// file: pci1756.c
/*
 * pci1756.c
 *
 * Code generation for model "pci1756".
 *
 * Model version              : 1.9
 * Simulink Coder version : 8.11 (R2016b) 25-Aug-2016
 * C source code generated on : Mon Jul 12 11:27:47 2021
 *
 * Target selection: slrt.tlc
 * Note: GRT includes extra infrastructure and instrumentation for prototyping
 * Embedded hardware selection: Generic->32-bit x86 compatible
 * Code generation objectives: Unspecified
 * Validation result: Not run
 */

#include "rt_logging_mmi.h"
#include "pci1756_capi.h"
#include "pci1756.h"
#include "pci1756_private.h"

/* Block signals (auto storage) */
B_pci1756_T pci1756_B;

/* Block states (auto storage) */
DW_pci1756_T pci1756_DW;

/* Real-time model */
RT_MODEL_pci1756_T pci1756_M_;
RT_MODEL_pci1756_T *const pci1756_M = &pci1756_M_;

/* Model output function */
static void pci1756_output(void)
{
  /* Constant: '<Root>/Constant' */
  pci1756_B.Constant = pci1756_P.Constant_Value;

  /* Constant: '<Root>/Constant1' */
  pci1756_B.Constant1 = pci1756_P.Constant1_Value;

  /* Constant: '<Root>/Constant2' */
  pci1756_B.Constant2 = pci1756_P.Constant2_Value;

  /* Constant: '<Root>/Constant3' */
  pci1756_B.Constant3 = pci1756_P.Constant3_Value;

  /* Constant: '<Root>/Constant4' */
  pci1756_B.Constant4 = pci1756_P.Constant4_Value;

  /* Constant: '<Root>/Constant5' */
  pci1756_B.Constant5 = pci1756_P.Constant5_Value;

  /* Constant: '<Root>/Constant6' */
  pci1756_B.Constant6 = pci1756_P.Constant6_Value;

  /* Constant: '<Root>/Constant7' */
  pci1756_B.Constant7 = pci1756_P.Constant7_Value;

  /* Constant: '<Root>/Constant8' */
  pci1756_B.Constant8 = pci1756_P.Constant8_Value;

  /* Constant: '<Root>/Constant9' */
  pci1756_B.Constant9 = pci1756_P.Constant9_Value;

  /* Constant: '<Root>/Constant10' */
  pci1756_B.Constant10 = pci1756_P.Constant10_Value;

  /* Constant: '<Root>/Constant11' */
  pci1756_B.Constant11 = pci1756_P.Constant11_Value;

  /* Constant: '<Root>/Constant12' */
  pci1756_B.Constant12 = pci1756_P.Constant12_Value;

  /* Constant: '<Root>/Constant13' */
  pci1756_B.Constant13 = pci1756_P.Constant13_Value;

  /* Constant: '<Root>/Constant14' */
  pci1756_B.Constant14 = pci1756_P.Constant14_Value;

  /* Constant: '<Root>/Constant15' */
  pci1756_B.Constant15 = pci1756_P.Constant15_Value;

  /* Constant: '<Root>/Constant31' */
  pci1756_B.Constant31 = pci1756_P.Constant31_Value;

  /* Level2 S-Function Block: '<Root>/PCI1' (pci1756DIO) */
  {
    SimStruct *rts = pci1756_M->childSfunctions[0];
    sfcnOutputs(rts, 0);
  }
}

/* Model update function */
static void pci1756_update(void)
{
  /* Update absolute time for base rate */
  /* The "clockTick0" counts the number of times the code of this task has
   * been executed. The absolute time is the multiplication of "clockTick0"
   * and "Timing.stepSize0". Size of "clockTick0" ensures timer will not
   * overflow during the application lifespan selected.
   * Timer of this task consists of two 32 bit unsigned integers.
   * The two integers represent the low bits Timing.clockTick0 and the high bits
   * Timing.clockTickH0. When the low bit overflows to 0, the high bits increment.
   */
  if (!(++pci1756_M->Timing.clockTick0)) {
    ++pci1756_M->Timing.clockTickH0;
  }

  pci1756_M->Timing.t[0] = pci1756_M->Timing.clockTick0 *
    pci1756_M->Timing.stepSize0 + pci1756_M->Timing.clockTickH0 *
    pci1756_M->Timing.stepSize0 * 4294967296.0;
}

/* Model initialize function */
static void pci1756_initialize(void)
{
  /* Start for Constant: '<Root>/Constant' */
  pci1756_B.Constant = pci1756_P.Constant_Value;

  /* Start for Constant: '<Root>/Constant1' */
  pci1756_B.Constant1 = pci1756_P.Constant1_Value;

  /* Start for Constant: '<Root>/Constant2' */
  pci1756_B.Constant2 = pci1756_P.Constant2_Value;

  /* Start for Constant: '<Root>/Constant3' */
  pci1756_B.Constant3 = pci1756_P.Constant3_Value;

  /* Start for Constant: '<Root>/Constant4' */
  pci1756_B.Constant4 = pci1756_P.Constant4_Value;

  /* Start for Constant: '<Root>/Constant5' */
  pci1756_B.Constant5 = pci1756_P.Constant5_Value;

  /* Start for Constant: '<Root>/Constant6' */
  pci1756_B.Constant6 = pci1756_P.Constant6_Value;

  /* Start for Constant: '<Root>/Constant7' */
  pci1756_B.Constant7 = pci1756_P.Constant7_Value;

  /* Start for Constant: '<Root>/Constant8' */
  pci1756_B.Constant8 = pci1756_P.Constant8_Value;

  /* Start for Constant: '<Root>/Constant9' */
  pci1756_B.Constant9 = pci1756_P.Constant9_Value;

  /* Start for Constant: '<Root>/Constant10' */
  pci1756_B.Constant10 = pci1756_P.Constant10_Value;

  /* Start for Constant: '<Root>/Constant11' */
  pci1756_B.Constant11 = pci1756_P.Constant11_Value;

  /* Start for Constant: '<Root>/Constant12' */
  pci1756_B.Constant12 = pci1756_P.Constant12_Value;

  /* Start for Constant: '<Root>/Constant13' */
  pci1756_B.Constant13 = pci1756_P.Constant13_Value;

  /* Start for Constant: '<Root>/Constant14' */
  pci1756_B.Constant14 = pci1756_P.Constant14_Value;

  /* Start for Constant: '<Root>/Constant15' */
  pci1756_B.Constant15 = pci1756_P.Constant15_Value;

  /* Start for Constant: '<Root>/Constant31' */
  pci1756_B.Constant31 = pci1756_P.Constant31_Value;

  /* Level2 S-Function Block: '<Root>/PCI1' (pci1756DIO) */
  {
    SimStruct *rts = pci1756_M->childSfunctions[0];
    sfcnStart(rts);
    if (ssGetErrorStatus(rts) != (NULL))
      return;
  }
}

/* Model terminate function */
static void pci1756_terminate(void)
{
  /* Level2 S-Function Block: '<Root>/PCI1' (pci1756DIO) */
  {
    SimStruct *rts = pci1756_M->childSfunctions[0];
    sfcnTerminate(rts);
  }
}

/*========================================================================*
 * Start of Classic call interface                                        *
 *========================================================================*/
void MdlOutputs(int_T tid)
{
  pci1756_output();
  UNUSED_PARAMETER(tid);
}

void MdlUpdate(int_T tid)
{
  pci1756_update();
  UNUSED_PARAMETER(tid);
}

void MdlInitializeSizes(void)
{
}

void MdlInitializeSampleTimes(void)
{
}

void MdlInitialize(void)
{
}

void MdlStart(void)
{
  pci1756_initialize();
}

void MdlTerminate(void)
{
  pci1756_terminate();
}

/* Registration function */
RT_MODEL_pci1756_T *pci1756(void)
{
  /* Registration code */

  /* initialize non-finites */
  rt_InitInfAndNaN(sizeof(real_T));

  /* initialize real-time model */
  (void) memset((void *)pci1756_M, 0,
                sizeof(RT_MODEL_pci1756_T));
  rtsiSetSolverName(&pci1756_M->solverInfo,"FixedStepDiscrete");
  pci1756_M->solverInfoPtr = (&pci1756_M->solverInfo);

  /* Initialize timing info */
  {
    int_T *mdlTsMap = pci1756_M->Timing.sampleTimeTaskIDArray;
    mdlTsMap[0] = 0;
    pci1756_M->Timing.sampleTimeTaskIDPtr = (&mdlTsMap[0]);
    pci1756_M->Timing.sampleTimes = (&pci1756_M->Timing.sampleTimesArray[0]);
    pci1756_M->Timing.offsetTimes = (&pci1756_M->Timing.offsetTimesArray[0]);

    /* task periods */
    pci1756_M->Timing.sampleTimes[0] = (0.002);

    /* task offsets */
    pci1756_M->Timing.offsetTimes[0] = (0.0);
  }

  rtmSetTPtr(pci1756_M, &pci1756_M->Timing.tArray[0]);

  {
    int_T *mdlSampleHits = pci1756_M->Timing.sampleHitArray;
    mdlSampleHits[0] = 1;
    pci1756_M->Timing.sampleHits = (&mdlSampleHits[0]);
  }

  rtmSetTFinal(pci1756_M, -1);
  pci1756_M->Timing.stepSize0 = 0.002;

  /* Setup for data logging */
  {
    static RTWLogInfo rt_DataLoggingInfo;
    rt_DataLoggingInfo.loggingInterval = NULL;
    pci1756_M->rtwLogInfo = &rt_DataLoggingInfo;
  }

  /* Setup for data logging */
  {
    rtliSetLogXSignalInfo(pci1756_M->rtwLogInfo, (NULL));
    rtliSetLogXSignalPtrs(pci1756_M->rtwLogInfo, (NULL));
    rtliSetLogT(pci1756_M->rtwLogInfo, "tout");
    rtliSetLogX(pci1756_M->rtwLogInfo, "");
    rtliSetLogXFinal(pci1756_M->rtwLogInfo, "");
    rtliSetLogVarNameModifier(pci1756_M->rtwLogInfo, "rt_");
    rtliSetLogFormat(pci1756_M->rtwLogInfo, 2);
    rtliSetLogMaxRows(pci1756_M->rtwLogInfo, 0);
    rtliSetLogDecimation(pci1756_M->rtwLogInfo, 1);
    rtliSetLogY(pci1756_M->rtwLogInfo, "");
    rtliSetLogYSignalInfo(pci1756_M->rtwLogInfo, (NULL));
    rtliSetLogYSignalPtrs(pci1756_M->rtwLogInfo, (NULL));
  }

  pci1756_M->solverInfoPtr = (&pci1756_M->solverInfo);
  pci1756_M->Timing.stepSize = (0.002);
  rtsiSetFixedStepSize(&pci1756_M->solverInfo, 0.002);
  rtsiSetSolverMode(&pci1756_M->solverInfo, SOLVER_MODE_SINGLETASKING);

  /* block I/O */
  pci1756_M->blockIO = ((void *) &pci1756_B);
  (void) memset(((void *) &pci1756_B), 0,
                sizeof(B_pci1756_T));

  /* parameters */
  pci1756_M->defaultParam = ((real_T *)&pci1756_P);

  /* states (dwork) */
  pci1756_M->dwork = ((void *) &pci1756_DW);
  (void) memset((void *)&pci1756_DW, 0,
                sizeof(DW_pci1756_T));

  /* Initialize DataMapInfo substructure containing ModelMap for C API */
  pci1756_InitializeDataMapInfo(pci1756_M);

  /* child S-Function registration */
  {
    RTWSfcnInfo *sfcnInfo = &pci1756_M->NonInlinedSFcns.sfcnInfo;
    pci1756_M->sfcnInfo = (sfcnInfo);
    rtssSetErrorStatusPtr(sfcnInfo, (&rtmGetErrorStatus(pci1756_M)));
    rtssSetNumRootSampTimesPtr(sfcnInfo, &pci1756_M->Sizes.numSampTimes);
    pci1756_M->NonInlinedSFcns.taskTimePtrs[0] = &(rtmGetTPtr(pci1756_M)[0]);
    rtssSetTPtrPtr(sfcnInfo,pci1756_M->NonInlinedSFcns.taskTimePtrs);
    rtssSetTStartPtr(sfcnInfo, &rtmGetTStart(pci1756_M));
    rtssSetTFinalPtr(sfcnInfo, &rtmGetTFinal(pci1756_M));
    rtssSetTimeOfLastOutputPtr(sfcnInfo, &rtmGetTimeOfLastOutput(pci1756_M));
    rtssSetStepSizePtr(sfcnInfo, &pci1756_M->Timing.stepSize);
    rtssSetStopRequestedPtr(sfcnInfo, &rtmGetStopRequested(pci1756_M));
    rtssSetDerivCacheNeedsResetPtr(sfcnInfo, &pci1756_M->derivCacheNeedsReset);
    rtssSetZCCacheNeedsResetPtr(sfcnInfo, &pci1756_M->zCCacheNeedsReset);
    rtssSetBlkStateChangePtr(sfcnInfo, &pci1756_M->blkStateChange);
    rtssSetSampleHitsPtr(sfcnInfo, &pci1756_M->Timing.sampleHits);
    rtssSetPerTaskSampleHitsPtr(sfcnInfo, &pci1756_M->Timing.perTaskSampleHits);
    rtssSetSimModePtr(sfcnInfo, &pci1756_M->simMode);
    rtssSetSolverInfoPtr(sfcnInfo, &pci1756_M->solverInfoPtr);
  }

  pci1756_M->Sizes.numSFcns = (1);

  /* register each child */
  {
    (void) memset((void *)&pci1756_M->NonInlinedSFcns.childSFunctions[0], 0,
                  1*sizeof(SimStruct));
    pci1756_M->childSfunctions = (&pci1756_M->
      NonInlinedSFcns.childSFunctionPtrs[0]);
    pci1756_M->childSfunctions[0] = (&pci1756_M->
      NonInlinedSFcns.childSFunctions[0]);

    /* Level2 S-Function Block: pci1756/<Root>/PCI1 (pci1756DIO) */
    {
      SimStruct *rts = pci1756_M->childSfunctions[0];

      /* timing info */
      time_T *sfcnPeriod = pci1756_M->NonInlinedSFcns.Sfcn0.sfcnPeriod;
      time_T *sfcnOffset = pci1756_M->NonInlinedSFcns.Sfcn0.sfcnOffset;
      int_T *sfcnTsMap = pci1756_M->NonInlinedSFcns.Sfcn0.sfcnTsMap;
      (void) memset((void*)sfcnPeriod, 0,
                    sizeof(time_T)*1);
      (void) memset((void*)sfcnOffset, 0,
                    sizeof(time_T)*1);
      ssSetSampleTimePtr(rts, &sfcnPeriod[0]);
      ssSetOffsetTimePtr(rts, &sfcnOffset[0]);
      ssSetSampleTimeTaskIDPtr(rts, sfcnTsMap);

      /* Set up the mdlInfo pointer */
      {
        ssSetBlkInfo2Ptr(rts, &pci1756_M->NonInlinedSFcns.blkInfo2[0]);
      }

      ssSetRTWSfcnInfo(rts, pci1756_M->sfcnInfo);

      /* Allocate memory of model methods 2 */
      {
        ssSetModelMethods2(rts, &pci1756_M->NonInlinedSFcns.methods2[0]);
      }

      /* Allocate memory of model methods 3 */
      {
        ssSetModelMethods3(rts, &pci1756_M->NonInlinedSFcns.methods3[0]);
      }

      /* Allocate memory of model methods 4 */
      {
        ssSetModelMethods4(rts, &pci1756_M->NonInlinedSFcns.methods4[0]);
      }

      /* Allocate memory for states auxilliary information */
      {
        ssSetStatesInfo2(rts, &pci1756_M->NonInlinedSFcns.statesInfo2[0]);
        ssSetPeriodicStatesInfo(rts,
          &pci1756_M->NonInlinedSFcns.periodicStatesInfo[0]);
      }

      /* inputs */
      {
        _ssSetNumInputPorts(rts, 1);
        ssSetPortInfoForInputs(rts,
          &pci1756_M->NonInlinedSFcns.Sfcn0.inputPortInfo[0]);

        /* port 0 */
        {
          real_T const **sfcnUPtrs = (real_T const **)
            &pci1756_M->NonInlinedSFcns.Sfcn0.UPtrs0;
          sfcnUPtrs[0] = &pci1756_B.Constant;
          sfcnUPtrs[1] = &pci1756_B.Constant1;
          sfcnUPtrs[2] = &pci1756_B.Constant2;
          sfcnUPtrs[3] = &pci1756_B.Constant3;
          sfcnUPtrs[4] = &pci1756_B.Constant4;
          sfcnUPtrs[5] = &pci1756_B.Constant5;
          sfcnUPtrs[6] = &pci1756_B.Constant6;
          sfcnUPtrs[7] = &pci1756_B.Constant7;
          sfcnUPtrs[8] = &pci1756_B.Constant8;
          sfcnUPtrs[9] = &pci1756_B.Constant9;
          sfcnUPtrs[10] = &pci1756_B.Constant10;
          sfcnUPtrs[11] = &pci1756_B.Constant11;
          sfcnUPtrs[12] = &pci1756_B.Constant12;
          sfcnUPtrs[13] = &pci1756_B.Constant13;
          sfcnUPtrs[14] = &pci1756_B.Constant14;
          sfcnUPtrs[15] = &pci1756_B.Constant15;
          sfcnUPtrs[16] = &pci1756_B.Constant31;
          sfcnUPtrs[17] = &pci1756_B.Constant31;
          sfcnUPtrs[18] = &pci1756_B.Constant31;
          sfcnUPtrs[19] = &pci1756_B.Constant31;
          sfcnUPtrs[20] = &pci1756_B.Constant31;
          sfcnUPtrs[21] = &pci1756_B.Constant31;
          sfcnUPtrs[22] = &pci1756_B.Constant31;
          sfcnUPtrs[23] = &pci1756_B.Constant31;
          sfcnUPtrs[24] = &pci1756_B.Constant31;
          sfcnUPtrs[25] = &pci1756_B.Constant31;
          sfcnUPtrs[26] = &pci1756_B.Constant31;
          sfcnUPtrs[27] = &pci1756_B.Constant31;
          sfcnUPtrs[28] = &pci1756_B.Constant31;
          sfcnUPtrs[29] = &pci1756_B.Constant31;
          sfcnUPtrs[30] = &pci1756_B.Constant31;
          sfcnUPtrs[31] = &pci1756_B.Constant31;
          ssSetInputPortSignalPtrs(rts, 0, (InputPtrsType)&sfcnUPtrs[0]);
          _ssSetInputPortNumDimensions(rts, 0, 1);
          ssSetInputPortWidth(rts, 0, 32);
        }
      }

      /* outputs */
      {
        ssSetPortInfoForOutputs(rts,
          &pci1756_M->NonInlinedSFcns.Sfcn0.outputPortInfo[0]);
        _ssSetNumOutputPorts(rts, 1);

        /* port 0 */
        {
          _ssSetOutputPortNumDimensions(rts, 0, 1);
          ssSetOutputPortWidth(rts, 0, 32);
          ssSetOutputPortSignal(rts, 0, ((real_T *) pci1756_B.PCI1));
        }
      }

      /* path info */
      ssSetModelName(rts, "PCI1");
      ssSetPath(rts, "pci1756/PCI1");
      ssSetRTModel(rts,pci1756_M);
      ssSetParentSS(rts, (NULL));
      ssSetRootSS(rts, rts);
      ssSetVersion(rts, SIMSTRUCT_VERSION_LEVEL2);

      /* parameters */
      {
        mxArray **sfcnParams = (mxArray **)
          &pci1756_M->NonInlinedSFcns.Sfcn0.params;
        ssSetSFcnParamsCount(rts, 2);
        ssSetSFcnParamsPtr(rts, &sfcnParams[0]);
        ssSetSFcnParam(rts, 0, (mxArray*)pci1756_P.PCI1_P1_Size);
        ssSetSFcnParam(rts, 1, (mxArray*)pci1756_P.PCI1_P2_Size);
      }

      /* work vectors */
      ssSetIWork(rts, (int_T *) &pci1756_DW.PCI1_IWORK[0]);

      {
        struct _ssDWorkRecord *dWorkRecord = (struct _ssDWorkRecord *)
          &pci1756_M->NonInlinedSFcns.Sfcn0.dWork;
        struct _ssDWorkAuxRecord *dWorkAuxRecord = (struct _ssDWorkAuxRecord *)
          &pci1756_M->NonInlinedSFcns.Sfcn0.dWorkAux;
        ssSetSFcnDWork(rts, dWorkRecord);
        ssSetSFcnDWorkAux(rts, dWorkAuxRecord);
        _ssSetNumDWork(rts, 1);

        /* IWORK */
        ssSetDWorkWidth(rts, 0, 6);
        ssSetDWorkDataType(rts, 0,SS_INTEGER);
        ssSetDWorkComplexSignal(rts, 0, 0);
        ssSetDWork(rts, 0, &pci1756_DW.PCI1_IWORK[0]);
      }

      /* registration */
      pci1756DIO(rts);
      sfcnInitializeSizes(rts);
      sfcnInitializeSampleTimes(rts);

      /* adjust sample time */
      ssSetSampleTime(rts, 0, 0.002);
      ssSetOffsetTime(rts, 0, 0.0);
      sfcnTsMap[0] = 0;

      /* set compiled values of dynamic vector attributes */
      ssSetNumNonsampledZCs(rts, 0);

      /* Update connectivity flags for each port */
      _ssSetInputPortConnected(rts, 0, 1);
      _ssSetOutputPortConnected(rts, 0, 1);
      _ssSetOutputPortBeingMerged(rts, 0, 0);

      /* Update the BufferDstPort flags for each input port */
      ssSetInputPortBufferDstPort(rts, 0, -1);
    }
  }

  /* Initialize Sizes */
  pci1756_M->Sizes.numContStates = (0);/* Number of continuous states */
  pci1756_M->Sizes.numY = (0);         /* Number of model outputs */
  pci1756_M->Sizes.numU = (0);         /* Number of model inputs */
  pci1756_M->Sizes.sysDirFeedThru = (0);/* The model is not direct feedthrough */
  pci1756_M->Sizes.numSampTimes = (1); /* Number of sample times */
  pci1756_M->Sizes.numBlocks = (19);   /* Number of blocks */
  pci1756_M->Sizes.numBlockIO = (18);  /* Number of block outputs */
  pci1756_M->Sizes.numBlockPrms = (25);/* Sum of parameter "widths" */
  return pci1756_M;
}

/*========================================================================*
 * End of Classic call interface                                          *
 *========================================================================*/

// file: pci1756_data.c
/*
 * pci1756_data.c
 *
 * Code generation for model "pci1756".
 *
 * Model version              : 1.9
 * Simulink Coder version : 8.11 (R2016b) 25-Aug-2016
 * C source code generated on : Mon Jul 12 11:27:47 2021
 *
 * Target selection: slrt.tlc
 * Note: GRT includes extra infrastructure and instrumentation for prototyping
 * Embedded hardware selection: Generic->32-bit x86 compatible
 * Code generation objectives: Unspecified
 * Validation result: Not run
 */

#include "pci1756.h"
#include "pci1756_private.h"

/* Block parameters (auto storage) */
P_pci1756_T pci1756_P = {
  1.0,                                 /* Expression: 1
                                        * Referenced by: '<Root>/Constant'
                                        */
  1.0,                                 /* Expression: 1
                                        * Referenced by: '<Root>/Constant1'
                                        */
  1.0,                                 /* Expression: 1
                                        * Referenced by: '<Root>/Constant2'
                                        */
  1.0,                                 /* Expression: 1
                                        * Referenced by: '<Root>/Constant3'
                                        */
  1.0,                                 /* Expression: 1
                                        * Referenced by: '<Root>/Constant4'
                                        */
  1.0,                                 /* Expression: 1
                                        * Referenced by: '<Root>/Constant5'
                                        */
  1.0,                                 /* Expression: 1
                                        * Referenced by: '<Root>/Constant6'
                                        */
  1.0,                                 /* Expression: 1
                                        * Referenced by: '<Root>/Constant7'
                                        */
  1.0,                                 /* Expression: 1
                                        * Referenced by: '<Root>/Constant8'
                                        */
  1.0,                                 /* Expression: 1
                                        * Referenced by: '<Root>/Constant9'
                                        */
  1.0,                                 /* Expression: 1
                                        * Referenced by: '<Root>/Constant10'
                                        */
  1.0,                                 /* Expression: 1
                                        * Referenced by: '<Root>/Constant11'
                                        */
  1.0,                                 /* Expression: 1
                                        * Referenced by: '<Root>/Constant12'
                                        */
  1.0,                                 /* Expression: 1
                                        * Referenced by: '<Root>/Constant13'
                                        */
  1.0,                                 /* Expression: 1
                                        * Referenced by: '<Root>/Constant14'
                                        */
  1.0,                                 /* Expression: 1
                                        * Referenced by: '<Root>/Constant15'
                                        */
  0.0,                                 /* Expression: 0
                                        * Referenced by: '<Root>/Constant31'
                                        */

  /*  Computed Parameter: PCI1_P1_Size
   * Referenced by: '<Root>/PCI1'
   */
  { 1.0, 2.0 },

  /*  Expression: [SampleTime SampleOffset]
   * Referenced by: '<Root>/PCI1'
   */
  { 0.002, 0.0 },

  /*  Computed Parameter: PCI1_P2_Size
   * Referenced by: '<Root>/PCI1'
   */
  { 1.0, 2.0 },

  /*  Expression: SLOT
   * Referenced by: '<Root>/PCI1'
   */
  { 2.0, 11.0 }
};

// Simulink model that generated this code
simulink model "pci1756"  (R2016b)
settings: Solver=ode4  StartTime=0.0  StopTime=inf  FixedStep=0.002  RelTol=1e-3  EnableMultiTasking=on

== system pci1756 ==
  note: 输出
  Constant{,1..15} (16 alike) : Constant
  Constant31 : Constant  Value=0
  Mux : Mux  Inputs=32
  PCI1 : S-Function  FunctionName=pci1756DIO  Parameters=[SampleTime SampleOffset], SLOT  SFunctionDeploymentMode=off  EnableBusSupport=off  mask(PCI1756){Sample=0.002, SLOT=[2 11]}
      mask prompts: Sample "Sample time:"
      mask help:
      | PCI-1756
      | Advantech
      | Digital Input&Output
      mask init:
      | SampleTime =0.002; SampleOffset=0;
  输入 : Display
  wires:
  Constant/1 -> Mux/1
  Constant1/1 -> Mux/2
  Constant2/1 -> Mux/3
  Constant3/1 -> Mux/4
  Constant4/1 -> Mux/5
  Constant5/1 -> Mux/6
  Constant6/1 -> Mux/7
  Constant7/1 -> Mux/8
  Constant8/1 -> Mux/9
  Constant9/1 -> Mux/10
  Constant10/1 -> Mux/11
  Constant11/1 -> Mux/12
  Constant12/1 -> Mux/13
  Constant13/1 -> Mux/14
  Constant14/1 -> Mux/15
  Constant15/1 -> Mux/16
  Constant31/1 -> Mux/32, Mux/31, Mux/30, Mux/29, Mux/28, Mux/27, Mux/26, Mux/25, Mux/24, Mux/23, Mux/22, Mux/21, Mux/20, Mux/19, Mux/17, Mux/18
  Mux/1 -> PCI1/1
  PCI1/1 -> 输入/1
